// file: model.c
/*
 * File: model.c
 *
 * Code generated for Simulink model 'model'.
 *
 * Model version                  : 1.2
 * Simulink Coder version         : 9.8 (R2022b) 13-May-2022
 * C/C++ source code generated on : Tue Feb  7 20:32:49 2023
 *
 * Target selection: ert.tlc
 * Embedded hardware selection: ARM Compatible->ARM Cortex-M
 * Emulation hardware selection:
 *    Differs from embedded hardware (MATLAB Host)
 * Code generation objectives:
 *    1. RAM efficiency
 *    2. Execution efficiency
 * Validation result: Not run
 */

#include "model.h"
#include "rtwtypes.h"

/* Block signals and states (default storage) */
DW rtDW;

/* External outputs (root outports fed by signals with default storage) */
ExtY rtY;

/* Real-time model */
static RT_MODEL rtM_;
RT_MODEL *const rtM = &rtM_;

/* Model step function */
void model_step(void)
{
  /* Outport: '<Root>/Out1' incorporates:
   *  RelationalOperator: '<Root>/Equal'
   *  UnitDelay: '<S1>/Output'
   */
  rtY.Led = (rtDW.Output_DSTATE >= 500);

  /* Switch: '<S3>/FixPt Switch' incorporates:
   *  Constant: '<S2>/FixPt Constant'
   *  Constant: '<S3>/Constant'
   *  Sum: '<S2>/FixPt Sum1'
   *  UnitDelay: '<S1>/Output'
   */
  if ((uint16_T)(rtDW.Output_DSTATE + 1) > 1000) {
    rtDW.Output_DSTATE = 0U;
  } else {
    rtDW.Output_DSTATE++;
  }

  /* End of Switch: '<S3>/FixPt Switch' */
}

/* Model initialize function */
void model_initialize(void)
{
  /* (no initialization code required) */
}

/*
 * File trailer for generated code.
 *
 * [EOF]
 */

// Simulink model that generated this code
simulink model "model"  (R2022b)
settings: Solver=FixedStepDiscrete  StartTime=0.0  StopTime=10000  RelTol=1e-3  EnableMultiTasking=on
model workspace (MAT data in the model file):
  mwTaskManagerKernelLatency = 1e-06
libraries: simulink x1

== system model ==
  Constant : Constant  Value=500
  Counter Limited : simulink/Sources/Counter Limited  uplimit=1000  tsamp=1
  Equal : RelationalOperator  OutDataTypeStr=boolean  RndMeth=Simplest  InputSameDT=off
  Scope : Scope
  Out1 : Outport
  wires:
  Counter Limited/1 -> Equal/1
  Equal/1 -> Scope/1, Out1/1
  Constant/1 -> Equal/2
